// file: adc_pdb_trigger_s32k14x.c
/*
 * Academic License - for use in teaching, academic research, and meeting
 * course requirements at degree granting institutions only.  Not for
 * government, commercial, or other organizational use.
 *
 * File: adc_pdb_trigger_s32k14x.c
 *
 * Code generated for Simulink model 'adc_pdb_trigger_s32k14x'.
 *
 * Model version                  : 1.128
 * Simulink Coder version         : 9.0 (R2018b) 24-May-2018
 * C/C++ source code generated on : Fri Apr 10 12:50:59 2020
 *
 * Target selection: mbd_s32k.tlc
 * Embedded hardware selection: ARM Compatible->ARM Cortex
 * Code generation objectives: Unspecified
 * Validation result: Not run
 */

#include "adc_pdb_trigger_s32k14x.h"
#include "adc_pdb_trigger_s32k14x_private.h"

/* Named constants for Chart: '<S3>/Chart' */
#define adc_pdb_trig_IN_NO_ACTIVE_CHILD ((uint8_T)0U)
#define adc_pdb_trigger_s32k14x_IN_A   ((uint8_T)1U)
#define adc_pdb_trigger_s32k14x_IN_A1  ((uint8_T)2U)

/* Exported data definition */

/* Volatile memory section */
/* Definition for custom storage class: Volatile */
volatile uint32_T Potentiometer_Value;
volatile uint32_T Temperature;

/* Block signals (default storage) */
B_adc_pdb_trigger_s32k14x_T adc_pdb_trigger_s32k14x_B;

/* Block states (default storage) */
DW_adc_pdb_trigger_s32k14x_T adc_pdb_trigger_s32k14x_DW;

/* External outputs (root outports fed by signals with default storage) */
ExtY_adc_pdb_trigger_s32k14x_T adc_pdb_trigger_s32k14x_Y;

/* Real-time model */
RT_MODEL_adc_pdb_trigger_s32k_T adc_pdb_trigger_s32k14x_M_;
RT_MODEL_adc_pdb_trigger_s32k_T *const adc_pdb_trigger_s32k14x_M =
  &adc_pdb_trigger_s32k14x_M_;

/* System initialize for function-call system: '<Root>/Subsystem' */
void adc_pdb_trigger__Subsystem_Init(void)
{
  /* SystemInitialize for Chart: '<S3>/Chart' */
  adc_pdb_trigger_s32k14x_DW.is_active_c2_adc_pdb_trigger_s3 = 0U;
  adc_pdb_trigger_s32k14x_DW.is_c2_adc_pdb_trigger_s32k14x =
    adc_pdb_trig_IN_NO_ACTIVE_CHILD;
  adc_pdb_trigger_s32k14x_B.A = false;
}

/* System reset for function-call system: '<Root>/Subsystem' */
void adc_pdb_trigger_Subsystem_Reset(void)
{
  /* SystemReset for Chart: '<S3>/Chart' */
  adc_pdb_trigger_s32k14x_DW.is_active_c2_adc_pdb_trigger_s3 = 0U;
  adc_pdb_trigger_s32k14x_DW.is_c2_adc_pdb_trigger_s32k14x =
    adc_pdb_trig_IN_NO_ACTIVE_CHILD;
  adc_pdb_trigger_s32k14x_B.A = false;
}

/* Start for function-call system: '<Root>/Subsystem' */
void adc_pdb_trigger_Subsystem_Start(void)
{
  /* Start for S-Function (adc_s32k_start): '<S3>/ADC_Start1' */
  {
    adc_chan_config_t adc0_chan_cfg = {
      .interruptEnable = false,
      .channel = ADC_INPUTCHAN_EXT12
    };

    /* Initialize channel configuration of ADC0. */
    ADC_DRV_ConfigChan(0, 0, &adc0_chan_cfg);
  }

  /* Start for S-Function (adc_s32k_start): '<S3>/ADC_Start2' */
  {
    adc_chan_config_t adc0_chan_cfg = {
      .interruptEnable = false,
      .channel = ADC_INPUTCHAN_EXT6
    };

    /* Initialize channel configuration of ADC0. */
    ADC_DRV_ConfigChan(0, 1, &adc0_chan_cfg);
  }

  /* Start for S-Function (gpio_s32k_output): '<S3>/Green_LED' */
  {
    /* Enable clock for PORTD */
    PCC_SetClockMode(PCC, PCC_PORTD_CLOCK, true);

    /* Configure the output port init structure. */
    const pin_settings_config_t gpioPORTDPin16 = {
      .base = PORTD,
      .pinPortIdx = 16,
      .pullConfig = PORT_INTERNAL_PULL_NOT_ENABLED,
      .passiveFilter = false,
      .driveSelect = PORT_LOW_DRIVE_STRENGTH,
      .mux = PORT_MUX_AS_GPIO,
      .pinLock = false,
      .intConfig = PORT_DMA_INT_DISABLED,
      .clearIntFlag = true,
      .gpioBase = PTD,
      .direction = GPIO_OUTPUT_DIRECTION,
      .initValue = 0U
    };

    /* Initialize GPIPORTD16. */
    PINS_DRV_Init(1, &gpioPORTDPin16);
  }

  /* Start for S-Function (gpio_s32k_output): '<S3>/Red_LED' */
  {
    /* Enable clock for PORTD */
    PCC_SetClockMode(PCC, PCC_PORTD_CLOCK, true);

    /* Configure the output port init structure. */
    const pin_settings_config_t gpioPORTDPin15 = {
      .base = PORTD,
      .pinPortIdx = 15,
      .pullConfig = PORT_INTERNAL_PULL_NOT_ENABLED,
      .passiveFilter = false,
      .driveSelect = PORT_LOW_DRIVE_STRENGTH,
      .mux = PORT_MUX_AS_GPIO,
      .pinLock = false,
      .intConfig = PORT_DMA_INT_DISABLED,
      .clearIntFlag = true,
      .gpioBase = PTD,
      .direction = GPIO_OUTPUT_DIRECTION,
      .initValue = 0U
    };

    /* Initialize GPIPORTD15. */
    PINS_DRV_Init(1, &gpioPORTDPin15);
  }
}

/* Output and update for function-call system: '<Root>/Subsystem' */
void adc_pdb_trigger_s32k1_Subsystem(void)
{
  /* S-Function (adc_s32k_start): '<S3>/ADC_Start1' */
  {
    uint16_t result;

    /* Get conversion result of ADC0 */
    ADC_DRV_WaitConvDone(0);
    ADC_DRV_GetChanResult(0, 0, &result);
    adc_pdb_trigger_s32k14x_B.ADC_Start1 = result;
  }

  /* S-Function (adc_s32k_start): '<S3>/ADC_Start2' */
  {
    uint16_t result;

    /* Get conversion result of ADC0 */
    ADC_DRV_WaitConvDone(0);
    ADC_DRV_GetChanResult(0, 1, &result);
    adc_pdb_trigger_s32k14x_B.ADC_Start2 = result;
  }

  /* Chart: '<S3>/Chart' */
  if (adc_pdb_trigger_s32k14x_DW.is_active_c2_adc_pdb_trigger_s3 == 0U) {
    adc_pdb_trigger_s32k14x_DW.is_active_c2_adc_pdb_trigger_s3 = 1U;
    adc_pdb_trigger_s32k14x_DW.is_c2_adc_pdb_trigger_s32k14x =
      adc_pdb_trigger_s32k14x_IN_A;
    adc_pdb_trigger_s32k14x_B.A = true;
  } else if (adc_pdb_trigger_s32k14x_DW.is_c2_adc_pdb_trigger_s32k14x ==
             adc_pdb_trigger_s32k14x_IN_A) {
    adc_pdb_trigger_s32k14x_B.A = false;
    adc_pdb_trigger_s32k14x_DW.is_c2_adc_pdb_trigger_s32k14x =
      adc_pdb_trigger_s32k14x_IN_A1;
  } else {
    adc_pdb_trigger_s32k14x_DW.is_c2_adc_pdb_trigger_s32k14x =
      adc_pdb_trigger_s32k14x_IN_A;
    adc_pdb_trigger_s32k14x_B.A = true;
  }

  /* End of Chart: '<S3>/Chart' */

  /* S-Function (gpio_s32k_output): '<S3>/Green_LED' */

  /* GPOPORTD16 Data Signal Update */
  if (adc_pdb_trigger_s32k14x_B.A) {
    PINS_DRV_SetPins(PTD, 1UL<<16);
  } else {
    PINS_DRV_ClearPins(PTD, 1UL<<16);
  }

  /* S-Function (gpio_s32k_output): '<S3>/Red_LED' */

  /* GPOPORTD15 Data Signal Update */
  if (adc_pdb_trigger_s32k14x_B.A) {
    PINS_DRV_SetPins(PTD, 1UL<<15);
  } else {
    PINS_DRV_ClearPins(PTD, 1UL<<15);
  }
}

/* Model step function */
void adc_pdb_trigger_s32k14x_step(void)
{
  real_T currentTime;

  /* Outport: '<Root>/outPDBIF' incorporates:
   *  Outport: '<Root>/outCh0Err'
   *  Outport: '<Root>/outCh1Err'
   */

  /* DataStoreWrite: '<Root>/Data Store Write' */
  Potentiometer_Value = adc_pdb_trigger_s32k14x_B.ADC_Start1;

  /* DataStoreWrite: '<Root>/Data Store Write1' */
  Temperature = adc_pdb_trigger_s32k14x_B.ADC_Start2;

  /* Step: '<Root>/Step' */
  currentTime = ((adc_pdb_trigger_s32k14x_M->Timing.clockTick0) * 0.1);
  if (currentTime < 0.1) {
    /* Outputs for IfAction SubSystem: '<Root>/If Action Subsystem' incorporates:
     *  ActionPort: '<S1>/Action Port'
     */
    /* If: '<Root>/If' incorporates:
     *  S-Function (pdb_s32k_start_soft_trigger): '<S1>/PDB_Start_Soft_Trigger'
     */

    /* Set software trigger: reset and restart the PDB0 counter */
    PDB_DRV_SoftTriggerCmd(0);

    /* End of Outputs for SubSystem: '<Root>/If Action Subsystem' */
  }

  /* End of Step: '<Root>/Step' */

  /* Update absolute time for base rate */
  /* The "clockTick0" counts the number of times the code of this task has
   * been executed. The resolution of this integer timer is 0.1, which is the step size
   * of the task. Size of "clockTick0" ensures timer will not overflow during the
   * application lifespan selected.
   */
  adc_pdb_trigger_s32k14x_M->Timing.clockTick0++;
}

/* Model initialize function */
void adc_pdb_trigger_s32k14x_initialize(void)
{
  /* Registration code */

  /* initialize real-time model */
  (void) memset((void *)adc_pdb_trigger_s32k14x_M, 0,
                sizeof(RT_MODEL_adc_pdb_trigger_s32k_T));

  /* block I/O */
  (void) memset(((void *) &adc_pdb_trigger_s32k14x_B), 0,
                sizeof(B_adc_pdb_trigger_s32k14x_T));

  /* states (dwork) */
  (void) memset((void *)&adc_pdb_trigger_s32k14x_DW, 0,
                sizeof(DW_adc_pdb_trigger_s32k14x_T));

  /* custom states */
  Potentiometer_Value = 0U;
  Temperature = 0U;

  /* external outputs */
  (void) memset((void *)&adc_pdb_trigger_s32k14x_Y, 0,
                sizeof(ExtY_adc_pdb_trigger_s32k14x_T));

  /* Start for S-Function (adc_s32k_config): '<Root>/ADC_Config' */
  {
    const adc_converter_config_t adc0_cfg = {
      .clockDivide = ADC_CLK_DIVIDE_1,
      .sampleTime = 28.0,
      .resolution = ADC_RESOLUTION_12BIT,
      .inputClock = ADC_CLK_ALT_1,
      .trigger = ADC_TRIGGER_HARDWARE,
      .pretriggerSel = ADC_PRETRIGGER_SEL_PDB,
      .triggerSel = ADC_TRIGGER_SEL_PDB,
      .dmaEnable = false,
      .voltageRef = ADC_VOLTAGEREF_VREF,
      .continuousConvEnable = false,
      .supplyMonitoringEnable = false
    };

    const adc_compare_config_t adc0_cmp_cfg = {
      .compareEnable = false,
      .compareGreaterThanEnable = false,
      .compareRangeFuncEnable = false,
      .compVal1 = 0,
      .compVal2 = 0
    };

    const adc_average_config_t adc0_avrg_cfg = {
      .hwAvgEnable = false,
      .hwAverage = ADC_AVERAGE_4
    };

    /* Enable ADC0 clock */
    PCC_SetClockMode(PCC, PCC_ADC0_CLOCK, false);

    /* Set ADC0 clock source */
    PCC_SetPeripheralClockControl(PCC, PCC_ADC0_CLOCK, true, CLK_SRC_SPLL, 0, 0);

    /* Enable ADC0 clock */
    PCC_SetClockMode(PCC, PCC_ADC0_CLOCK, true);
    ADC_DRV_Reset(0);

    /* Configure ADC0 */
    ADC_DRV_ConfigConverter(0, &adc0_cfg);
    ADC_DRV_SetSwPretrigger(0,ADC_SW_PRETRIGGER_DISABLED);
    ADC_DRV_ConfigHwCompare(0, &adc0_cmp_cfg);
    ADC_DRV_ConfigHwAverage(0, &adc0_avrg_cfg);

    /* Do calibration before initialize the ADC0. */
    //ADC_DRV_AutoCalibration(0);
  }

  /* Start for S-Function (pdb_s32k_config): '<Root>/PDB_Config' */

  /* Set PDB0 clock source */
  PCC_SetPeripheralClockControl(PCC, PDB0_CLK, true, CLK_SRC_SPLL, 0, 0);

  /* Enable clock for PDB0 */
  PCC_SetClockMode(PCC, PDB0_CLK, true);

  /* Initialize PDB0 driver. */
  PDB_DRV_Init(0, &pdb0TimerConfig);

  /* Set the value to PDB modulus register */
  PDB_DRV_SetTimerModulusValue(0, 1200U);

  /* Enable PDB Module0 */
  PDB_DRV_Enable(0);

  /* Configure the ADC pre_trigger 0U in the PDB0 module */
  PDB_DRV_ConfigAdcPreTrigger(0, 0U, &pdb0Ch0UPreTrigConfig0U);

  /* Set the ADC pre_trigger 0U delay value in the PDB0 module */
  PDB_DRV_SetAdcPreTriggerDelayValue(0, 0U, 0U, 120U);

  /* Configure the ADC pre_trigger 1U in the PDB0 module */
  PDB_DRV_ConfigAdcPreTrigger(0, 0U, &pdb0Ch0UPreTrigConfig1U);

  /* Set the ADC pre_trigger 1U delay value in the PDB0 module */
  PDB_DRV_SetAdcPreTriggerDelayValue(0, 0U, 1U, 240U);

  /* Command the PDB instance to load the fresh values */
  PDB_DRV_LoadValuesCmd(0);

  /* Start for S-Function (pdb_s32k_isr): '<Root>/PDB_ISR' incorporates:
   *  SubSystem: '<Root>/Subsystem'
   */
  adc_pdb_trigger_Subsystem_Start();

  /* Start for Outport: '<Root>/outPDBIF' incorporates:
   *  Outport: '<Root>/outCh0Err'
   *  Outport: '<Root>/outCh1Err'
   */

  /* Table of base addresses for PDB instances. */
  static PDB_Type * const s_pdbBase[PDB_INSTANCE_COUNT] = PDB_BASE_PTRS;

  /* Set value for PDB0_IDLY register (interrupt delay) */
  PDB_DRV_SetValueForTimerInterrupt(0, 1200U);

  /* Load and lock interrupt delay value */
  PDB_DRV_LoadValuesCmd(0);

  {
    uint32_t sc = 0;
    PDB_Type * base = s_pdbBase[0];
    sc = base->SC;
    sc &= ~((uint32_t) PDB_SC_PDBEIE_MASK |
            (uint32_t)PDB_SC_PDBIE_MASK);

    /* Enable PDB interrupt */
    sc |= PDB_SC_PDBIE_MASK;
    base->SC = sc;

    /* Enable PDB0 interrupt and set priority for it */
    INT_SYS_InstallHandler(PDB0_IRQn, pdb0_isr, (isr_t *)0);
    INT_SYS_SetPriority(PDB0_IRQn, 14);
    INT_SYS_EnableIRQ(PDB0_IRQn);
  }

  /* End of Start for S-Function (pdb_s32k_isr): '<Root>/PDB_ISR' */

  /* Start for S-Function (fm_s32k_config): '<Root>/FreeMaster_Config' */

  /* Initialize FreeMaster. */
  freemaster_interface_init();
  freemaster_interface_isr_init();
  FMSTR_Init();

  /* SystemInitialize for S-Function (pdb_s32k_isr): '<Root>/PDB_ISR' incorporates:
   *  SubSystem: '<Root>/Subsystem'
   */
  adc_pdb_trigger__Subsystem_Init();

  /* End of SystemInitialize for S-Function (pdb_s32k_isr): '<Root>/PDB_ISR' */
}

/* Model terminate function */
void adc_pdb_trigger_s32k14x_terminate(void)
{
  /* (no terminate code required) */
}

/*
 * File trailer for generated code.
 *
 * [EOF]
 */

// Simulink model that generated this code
simulink model "adc_pdb_trigger_s32k14x"  (Simulink 9.2)
settings: Solver=FixedStepDiscrete  StartTime=0.0  StopTime=10.0  FixedStep=0.1  RelTol=1e-3  EnableMultiTasking=on
InitFcn:
  | mbd_s32k_consistency_checks(bdroot(gcs));
undefined symbols (not defined in the file): LQFP
libraries: mbd_s32k1xx_ec_toolbox x10, simulink x1

== system adc_pdb_trigger_s32k14x ==
  note: S32K14x EVB Config and example description
  ADC_Config : mbd_s32k1xx_ec_toolbox/Motor Control Blocks/ADC Blocks/ADC_Config  Priority=1  instance=0  mode=12-bit conversion  smplts=29  adiclk=alternate clock 1  adiv=input clock  show_adv_opts=on  pretrgsel=PDB pre-trigger  swpretrg=Disabled  adtrg=hardware  trgsel=PDB output  refsel=Vrefh and Vrefl  supply_monitoring=off  acfe=off  acfgt=off  acren=off  cv1=0  cv2=0  adco=off  avge=off  avgs=4 samples
  Data Store Memory : DataStoreMemory  DataStoreName=Potentiometer_Value  ReadBeforeWriteMsg=warning  WriteAfterWriteMsg=warning  WriteAfterReadMsg=warning  ShowAdditionalParam=off  OutDataTypeStr=uint32
  Data Store Memory1 : DataStoreMemory  DataStoreName=Temperature  ReadBeforeWriteMsg=warning  WriteAfterWriteMsg=warning  WriteAfterReadMsg=warning  ShowAdditionalParam=off  OutDataTypeStr=uint32
  Data Store Write : DataStoreWrite  DataStoreName=Potentiometer_Value
  Data Store Write1 : DataStoreWrite  DataStoreName=Temperature
  FreeMaster_Config : mbd_s32k1xx_ec_toolbox/Utility Blocks/FreeMaster_Config  interface=LPUART1  baudrate=115200  rxd=PTC6: [LPUART1_RX | Receive]  txd=PTC7: [LPUART1_TX | Transmit]  mode=Short Interrupt  isr_prio=15  show_adv_opts=off  use_scope=on  max_scope_vars=8  use_recorder=on  max_rec_vars=8  rec_buff_size=1024  rec_timebase=0 milliseconds  comm_buffer_size_auto=on  comm_buffer_size=255  comm_rqueue_size_default=on  comm_rqueue_size=32
  If : If  IfExpression=u1 == 1  ShowElse=off
  If Action Subsystem : Subsystem  TreatAsAtomicUnit=on
  MBD_S32K14x_Config_Information : mbd_s32k1xx_ec_toolbox/MBD_S32K1xx_Config_Information  mbdt_ver=0  disp_str=|  config_params=[]  mcu_target_name=S32K144  mcu_target_package=100-LQFP  mcu_target_sram_size=64KB  mcu_system_clock_freq=80  mcu_xtal_freq=External 8  mcu_steptick_timer=LPIT Channel 0  mcu_steptick_prio=15  ds_import_enable=on  target_compiler=GCC  target_memory=FLASH  gcc_target_compile_opts=-mcpu=cortex-m4 -mthumb -mfloat-abi=hard -mfpu=fpv4-sp-d16 -O1 -g -gstrict-dwarf  gcc_target_assemble_opts=-mcpu=cortex-m4 -mthumb -mfloat-abi=hard -mfpu=fpv4-sp-d16 -g  gcc_target_link_opts=-mcpu=cortex-m4 -mthumb -mfloat-abi=hard -mfpu=fpv4-sp-d16  gcc_target_default_lcf=on  gcc_target_user_lcf=S32K144_64_flash.ld  ghs_target_compile_opts=-cpu=cortexm4f -thumb -DARM_MATH_CM4 -fpu=vfpv4_d16 -fsingle -Ogeneral -Wundef -Wimplicit-int -Wshadow -Wtrigraphs --no_commons --gnu_asm -gnu99 -gdwarf-2 -G  ghs_target_assemble_opts=-cpu=cortexm4f -fpu=vfpv4_d16  ghs_target_link_opts=-cpu=cortexm4f -thumb -fpu=vfpv4_d16  ghs_target_default_lcf=on  ghs_target_user_lcf=S32K144_64_flash.ld  iar_target_compile_opts=--cpu=Cortex-M4F --thumb --fpu=VFPv4_sp -Ol -e --debug --dlib_config normal  iar_target_assemble_opts=--cpu Cortex-M4F --thumb --fpu VFPv4_sp  iar_target_link_opts=--no_exceptions --vfe --inline  iar_target_default_lcf=on  iar_target_user_lcf=S32K144_64_flash.icf  pil_download_enable=off  rbl_download_enable=on  rbl_start_delay=5000000  rbl_download_interface=OpenSDA  rbl_restart_request=off  rbl_com_port=Custom  rbl_com_port_custom=COM1  pil_download_rate=57600  pil_opensda_drive=D: EVB-S32K144  pil_opensda_drive_custom=D  pil_uart_instance=1  pil_uart_rx=PTC6: [LPUART1_RX | Receive]  pil_uart_tx=PTC7: [LPUART1_TX | Transmit]  FTM_PWM_PcrCheckEnDis=on  FTM_Input_Edge_Inputs_PcrCheckEnDis=on  FTM_Dual_Edge_Inputs_PcrCheckEnDis=on  FTM_Quadrature_Inputs_PcrCheckEnDis=on  FTM_Hall_Sensor_Inputs_PcrCheckEnDis=on  LPTMR_PcrCheckEnDis=on  PIT_PcrCheckEnDis=on  RTC_PcrCheckEnDis=on  FlexCAN_PcrCheckEnDis=on  LIN_PcrCheckEnDis=on  FlexIO_PcrCheckEnDis=on  LPI2C_PcrCheckEnDis=on  LPSPI_PcrCheckEnDis=on  LPUART_PcrCheckEnDis=on  CMP_PcrCheckEnDis=on  GPIO_OutputPcrCheckEnDis=on  GPIO_InputPcrCheckEnDis=on  SBC_PcrCheckEnDis=on  AMMCLIB_PcrCheckEnDis=on  FM_PcrCheckEnDis=on  Profile_PcrCheckEnDis=on  ConfigParams_PcrCheckEnDis=on  ModelRef_PcrCheckEnDis=on  PDB0_PcrCheckEnDis=on  CSEc_PcrCheckEnDis=on  eDMA_PcrCheckEnDis=on  ADC_PcrCheckEnDis=on  WDOG_PcrCheckEnDis=on
      | Target : S32K144-64KB_SRAM
      | Package : 100-pin
      | System clock : 80 MHz
      | XTAL clock : External 8 MHz
      | Compiler : GreenHills Multi
      | Target Type : FLASH
      | Download Code after build : (OpenSDA: F)
      | Step Tick Interrupt Priority : 15
  Model Info : simulink/Model-Wide Utilities/Model Info  Frame=off  DisplayStringWithTags=|  HorizontalTextAlignment=Left  LeftAlignmentValue=0.02
      | Model Name: %<ModelName>
      | 
      | Description: %<Description>
  PDB_Config : mbd_s32k1xx_ec_toolbox/Motor Control Blocks/PDB Blocks/PDB_Config  Priority=1  pdbModule=0  regScCont=Continuous  regScTrgsel=Software  trgMuxSel=FTM2 External Trigger  trgMuxSelPin=PTB5: [TRGMUX_IN0 | Trigger Mux Input]  regModModulus=1200  regScPrescaler=128  regScMult=40  regPoenPoen0=off  regPo0DlyDly1=0  regPo0DlyDly2=0  enable_pdb_init=on  show_adv_opts=off  regCh0C1En0=on  regCh0C1En1=on  regCh0C1En2=off  regCh0C1En3=off  regCh0C1En4=off  regCh0C1En5=off  regCh0C1En6=off  regCh0C1En7=off  regCh0C1Bb0=off  regCh0C1Bb1=off  regCh0C1Bb2=off  regCh0C1Bb3=off  regCh0C1Bb4=off  regCh0C1Bb5=off  regCh0C1Bb6=off  regCh0C1Bb7=off  regCh0C1Tos0=Pre-trigger is in delay mode  regCh0C1Tos1=Pre-trigger is in delay mode  regCh0C1Tos2=Pre-trigger is in delay mode  regCh0C1Tos3=Pre-trigger is in delay mode  regCh0C1Tos4=Pre-trigger is in delay mode  regCh0C1Tos5=Pre-trigger is in delay mode  regCh0C1Tos6=Pre-trigger is in delay mode  regCh0C1Tos7=Pre-trigger is in delay mode  regCh0DlyDly0=120  regCh0DlyDly1=240  regCh0DlyDly2=5000  regCh0DlyDly3=10000  regCh0DlyDly4=0  regCh0DlyDly5=0  regCh0DlyDly6=0  regCh0DlyDly7=0  regCh1C1En0=off  regCh1C1En1=off  regCh1C1En2=off  regCh1C1En3=off  regCh1C1En4=off  regCh1C1En5=off  regCh1C1En6=off  regCh1C1En7=off  regCh1C1Bb0=off  regCh1C1Bb1=off  regCh1C1Bb2=off  regCh1C1Bb3=off  regCh1C1Bb4=off  regCh1C1Bb5=off  regCh1C1Bb6=off  regCh1C1Bb7=off  regCh1C1Tos0=Pre-trigger is in delay mode  regCh1C1Tos1=Pre-trigger is in delay mode  regCh1C1Tos2=Pre-trigger is in delay mode  regCh1C1Tos3=Pre-trigger is in delay mode  regCh1C1Tos4=Pre-trigger is in delay mode  regCh1C1Tos5=Pre-trigger is in delay mode  regCh1C1Tos6=Pre-trigger is in delay mode  regCh1C1Tos7=Pre-trigger is in delay mode  regCh1DlyDly0=0  regCh1DlyDly1=0  regCh1DlyDly2=0  regCh1DlyDly3=0  regCh1DlyDly4=0  regCh1DlyDly5=0  regCh1DlyDly6=0  regCh1DlyDly7=0
  PDB_ISR : mbd_s32k1xx_ec_toolbox/Motor Control Blocks/PDB Blocks/PDB_ISR  Priority=2  pdbModule=0  prioInterrupt=14  regScPdbie=on  regScPdbeie=off  regIdlyIdly=1200
  Step : Step  Time=str2num(get_param(bdroot, 'FixedStep'))  Before=1  After=2
  Subsystem : Subsystem  TreatAsAtomicUnit=on
  outPDBIF : Outport
  outCh0Err : Outport  Port=2
  outCh1Err : Outport  Port=3
  wires:
  Step/1 -> If/1
  If/1 -> If Action Subsystem/Action
  PDB_ISR/2 -> outPDBIF/1
  PDB_ISR/4 -> outCh1Err/1
  PDB_ISR/3 -> outCh0Err/1
  PDB_ISR/1 -> Subsystem/Trigger
  Subsystem/1(potentiometer) -> Data Store Write/1
  Subsystem/2(temperature) -> Data Store Write1/1

== system adc_pdb_trigger_s32k14x/If Action Subsystem ==
  Action Port : ActionPort
  PDB_Start_Soft_Trigger : mbd_s32k1xx_ec_toolbox/Motor Control Blocks/PDB Blocks/PDB_Start_Soft_Trigger  Priority=9  pdbModule=0

== system adc_pdb_trigger_s32k14x/Subsystem ==
  function : TriggerPort  TriggerType=function-call  VariantControl=Variant
  ADC_Start1 : mbd_s32k1xx_ec_toolbox/Motor Control Blocks/ADC Blocks/ADC_Start  instance=0  adc_r=A  adc_chan=PTC14: [ADC0_SE12 | ADC Single Ended Input]  aien=off  mcuTargetUpdate=on
  ADC_Start2 : mbd_s32k1xx_ec_toolbox/Motor Control Blocks/ADC Blocks/ADC_Start  instance=0  adc_r=B  adc_chan=PTB2: [ADC0_SE6 | ADC Single Ended Input]  aien=off  mcuTargetUpdate=on
  Chart : Stateflow chart  TreatAsAtomicUnit=on
  Green_LED : mbd_s32k1xx_ec_toolbox/GPIO Blocks/Digital_Output  gpio_pin=PTD16: [PTD16 | Port D I/O]  init_val=Low  drive_strength=Low
  Red_LED : mbd_s32k1xx_ec_toolbox/GPIO Blocks/Digital_Output  gpio_pin=PTD15: [PTD15 | Port D I/O]  init_val=Low  drive_strength=Low
  potentiometer : Outport
  temperature : Outport  Port=2
  wires:
  Chart/1(" A") -> Green_LED/1, Red_LED/1
  ADC_Start1/1 -> potentiometer/1
  ADC_Start2/1 -> temperature/1

== stateflow chart Subsystem/Chart ==
  state A
  state A1
  (default) -> A
  A -> A1
  A1 -> A
  data: A output boolean [0..1]
